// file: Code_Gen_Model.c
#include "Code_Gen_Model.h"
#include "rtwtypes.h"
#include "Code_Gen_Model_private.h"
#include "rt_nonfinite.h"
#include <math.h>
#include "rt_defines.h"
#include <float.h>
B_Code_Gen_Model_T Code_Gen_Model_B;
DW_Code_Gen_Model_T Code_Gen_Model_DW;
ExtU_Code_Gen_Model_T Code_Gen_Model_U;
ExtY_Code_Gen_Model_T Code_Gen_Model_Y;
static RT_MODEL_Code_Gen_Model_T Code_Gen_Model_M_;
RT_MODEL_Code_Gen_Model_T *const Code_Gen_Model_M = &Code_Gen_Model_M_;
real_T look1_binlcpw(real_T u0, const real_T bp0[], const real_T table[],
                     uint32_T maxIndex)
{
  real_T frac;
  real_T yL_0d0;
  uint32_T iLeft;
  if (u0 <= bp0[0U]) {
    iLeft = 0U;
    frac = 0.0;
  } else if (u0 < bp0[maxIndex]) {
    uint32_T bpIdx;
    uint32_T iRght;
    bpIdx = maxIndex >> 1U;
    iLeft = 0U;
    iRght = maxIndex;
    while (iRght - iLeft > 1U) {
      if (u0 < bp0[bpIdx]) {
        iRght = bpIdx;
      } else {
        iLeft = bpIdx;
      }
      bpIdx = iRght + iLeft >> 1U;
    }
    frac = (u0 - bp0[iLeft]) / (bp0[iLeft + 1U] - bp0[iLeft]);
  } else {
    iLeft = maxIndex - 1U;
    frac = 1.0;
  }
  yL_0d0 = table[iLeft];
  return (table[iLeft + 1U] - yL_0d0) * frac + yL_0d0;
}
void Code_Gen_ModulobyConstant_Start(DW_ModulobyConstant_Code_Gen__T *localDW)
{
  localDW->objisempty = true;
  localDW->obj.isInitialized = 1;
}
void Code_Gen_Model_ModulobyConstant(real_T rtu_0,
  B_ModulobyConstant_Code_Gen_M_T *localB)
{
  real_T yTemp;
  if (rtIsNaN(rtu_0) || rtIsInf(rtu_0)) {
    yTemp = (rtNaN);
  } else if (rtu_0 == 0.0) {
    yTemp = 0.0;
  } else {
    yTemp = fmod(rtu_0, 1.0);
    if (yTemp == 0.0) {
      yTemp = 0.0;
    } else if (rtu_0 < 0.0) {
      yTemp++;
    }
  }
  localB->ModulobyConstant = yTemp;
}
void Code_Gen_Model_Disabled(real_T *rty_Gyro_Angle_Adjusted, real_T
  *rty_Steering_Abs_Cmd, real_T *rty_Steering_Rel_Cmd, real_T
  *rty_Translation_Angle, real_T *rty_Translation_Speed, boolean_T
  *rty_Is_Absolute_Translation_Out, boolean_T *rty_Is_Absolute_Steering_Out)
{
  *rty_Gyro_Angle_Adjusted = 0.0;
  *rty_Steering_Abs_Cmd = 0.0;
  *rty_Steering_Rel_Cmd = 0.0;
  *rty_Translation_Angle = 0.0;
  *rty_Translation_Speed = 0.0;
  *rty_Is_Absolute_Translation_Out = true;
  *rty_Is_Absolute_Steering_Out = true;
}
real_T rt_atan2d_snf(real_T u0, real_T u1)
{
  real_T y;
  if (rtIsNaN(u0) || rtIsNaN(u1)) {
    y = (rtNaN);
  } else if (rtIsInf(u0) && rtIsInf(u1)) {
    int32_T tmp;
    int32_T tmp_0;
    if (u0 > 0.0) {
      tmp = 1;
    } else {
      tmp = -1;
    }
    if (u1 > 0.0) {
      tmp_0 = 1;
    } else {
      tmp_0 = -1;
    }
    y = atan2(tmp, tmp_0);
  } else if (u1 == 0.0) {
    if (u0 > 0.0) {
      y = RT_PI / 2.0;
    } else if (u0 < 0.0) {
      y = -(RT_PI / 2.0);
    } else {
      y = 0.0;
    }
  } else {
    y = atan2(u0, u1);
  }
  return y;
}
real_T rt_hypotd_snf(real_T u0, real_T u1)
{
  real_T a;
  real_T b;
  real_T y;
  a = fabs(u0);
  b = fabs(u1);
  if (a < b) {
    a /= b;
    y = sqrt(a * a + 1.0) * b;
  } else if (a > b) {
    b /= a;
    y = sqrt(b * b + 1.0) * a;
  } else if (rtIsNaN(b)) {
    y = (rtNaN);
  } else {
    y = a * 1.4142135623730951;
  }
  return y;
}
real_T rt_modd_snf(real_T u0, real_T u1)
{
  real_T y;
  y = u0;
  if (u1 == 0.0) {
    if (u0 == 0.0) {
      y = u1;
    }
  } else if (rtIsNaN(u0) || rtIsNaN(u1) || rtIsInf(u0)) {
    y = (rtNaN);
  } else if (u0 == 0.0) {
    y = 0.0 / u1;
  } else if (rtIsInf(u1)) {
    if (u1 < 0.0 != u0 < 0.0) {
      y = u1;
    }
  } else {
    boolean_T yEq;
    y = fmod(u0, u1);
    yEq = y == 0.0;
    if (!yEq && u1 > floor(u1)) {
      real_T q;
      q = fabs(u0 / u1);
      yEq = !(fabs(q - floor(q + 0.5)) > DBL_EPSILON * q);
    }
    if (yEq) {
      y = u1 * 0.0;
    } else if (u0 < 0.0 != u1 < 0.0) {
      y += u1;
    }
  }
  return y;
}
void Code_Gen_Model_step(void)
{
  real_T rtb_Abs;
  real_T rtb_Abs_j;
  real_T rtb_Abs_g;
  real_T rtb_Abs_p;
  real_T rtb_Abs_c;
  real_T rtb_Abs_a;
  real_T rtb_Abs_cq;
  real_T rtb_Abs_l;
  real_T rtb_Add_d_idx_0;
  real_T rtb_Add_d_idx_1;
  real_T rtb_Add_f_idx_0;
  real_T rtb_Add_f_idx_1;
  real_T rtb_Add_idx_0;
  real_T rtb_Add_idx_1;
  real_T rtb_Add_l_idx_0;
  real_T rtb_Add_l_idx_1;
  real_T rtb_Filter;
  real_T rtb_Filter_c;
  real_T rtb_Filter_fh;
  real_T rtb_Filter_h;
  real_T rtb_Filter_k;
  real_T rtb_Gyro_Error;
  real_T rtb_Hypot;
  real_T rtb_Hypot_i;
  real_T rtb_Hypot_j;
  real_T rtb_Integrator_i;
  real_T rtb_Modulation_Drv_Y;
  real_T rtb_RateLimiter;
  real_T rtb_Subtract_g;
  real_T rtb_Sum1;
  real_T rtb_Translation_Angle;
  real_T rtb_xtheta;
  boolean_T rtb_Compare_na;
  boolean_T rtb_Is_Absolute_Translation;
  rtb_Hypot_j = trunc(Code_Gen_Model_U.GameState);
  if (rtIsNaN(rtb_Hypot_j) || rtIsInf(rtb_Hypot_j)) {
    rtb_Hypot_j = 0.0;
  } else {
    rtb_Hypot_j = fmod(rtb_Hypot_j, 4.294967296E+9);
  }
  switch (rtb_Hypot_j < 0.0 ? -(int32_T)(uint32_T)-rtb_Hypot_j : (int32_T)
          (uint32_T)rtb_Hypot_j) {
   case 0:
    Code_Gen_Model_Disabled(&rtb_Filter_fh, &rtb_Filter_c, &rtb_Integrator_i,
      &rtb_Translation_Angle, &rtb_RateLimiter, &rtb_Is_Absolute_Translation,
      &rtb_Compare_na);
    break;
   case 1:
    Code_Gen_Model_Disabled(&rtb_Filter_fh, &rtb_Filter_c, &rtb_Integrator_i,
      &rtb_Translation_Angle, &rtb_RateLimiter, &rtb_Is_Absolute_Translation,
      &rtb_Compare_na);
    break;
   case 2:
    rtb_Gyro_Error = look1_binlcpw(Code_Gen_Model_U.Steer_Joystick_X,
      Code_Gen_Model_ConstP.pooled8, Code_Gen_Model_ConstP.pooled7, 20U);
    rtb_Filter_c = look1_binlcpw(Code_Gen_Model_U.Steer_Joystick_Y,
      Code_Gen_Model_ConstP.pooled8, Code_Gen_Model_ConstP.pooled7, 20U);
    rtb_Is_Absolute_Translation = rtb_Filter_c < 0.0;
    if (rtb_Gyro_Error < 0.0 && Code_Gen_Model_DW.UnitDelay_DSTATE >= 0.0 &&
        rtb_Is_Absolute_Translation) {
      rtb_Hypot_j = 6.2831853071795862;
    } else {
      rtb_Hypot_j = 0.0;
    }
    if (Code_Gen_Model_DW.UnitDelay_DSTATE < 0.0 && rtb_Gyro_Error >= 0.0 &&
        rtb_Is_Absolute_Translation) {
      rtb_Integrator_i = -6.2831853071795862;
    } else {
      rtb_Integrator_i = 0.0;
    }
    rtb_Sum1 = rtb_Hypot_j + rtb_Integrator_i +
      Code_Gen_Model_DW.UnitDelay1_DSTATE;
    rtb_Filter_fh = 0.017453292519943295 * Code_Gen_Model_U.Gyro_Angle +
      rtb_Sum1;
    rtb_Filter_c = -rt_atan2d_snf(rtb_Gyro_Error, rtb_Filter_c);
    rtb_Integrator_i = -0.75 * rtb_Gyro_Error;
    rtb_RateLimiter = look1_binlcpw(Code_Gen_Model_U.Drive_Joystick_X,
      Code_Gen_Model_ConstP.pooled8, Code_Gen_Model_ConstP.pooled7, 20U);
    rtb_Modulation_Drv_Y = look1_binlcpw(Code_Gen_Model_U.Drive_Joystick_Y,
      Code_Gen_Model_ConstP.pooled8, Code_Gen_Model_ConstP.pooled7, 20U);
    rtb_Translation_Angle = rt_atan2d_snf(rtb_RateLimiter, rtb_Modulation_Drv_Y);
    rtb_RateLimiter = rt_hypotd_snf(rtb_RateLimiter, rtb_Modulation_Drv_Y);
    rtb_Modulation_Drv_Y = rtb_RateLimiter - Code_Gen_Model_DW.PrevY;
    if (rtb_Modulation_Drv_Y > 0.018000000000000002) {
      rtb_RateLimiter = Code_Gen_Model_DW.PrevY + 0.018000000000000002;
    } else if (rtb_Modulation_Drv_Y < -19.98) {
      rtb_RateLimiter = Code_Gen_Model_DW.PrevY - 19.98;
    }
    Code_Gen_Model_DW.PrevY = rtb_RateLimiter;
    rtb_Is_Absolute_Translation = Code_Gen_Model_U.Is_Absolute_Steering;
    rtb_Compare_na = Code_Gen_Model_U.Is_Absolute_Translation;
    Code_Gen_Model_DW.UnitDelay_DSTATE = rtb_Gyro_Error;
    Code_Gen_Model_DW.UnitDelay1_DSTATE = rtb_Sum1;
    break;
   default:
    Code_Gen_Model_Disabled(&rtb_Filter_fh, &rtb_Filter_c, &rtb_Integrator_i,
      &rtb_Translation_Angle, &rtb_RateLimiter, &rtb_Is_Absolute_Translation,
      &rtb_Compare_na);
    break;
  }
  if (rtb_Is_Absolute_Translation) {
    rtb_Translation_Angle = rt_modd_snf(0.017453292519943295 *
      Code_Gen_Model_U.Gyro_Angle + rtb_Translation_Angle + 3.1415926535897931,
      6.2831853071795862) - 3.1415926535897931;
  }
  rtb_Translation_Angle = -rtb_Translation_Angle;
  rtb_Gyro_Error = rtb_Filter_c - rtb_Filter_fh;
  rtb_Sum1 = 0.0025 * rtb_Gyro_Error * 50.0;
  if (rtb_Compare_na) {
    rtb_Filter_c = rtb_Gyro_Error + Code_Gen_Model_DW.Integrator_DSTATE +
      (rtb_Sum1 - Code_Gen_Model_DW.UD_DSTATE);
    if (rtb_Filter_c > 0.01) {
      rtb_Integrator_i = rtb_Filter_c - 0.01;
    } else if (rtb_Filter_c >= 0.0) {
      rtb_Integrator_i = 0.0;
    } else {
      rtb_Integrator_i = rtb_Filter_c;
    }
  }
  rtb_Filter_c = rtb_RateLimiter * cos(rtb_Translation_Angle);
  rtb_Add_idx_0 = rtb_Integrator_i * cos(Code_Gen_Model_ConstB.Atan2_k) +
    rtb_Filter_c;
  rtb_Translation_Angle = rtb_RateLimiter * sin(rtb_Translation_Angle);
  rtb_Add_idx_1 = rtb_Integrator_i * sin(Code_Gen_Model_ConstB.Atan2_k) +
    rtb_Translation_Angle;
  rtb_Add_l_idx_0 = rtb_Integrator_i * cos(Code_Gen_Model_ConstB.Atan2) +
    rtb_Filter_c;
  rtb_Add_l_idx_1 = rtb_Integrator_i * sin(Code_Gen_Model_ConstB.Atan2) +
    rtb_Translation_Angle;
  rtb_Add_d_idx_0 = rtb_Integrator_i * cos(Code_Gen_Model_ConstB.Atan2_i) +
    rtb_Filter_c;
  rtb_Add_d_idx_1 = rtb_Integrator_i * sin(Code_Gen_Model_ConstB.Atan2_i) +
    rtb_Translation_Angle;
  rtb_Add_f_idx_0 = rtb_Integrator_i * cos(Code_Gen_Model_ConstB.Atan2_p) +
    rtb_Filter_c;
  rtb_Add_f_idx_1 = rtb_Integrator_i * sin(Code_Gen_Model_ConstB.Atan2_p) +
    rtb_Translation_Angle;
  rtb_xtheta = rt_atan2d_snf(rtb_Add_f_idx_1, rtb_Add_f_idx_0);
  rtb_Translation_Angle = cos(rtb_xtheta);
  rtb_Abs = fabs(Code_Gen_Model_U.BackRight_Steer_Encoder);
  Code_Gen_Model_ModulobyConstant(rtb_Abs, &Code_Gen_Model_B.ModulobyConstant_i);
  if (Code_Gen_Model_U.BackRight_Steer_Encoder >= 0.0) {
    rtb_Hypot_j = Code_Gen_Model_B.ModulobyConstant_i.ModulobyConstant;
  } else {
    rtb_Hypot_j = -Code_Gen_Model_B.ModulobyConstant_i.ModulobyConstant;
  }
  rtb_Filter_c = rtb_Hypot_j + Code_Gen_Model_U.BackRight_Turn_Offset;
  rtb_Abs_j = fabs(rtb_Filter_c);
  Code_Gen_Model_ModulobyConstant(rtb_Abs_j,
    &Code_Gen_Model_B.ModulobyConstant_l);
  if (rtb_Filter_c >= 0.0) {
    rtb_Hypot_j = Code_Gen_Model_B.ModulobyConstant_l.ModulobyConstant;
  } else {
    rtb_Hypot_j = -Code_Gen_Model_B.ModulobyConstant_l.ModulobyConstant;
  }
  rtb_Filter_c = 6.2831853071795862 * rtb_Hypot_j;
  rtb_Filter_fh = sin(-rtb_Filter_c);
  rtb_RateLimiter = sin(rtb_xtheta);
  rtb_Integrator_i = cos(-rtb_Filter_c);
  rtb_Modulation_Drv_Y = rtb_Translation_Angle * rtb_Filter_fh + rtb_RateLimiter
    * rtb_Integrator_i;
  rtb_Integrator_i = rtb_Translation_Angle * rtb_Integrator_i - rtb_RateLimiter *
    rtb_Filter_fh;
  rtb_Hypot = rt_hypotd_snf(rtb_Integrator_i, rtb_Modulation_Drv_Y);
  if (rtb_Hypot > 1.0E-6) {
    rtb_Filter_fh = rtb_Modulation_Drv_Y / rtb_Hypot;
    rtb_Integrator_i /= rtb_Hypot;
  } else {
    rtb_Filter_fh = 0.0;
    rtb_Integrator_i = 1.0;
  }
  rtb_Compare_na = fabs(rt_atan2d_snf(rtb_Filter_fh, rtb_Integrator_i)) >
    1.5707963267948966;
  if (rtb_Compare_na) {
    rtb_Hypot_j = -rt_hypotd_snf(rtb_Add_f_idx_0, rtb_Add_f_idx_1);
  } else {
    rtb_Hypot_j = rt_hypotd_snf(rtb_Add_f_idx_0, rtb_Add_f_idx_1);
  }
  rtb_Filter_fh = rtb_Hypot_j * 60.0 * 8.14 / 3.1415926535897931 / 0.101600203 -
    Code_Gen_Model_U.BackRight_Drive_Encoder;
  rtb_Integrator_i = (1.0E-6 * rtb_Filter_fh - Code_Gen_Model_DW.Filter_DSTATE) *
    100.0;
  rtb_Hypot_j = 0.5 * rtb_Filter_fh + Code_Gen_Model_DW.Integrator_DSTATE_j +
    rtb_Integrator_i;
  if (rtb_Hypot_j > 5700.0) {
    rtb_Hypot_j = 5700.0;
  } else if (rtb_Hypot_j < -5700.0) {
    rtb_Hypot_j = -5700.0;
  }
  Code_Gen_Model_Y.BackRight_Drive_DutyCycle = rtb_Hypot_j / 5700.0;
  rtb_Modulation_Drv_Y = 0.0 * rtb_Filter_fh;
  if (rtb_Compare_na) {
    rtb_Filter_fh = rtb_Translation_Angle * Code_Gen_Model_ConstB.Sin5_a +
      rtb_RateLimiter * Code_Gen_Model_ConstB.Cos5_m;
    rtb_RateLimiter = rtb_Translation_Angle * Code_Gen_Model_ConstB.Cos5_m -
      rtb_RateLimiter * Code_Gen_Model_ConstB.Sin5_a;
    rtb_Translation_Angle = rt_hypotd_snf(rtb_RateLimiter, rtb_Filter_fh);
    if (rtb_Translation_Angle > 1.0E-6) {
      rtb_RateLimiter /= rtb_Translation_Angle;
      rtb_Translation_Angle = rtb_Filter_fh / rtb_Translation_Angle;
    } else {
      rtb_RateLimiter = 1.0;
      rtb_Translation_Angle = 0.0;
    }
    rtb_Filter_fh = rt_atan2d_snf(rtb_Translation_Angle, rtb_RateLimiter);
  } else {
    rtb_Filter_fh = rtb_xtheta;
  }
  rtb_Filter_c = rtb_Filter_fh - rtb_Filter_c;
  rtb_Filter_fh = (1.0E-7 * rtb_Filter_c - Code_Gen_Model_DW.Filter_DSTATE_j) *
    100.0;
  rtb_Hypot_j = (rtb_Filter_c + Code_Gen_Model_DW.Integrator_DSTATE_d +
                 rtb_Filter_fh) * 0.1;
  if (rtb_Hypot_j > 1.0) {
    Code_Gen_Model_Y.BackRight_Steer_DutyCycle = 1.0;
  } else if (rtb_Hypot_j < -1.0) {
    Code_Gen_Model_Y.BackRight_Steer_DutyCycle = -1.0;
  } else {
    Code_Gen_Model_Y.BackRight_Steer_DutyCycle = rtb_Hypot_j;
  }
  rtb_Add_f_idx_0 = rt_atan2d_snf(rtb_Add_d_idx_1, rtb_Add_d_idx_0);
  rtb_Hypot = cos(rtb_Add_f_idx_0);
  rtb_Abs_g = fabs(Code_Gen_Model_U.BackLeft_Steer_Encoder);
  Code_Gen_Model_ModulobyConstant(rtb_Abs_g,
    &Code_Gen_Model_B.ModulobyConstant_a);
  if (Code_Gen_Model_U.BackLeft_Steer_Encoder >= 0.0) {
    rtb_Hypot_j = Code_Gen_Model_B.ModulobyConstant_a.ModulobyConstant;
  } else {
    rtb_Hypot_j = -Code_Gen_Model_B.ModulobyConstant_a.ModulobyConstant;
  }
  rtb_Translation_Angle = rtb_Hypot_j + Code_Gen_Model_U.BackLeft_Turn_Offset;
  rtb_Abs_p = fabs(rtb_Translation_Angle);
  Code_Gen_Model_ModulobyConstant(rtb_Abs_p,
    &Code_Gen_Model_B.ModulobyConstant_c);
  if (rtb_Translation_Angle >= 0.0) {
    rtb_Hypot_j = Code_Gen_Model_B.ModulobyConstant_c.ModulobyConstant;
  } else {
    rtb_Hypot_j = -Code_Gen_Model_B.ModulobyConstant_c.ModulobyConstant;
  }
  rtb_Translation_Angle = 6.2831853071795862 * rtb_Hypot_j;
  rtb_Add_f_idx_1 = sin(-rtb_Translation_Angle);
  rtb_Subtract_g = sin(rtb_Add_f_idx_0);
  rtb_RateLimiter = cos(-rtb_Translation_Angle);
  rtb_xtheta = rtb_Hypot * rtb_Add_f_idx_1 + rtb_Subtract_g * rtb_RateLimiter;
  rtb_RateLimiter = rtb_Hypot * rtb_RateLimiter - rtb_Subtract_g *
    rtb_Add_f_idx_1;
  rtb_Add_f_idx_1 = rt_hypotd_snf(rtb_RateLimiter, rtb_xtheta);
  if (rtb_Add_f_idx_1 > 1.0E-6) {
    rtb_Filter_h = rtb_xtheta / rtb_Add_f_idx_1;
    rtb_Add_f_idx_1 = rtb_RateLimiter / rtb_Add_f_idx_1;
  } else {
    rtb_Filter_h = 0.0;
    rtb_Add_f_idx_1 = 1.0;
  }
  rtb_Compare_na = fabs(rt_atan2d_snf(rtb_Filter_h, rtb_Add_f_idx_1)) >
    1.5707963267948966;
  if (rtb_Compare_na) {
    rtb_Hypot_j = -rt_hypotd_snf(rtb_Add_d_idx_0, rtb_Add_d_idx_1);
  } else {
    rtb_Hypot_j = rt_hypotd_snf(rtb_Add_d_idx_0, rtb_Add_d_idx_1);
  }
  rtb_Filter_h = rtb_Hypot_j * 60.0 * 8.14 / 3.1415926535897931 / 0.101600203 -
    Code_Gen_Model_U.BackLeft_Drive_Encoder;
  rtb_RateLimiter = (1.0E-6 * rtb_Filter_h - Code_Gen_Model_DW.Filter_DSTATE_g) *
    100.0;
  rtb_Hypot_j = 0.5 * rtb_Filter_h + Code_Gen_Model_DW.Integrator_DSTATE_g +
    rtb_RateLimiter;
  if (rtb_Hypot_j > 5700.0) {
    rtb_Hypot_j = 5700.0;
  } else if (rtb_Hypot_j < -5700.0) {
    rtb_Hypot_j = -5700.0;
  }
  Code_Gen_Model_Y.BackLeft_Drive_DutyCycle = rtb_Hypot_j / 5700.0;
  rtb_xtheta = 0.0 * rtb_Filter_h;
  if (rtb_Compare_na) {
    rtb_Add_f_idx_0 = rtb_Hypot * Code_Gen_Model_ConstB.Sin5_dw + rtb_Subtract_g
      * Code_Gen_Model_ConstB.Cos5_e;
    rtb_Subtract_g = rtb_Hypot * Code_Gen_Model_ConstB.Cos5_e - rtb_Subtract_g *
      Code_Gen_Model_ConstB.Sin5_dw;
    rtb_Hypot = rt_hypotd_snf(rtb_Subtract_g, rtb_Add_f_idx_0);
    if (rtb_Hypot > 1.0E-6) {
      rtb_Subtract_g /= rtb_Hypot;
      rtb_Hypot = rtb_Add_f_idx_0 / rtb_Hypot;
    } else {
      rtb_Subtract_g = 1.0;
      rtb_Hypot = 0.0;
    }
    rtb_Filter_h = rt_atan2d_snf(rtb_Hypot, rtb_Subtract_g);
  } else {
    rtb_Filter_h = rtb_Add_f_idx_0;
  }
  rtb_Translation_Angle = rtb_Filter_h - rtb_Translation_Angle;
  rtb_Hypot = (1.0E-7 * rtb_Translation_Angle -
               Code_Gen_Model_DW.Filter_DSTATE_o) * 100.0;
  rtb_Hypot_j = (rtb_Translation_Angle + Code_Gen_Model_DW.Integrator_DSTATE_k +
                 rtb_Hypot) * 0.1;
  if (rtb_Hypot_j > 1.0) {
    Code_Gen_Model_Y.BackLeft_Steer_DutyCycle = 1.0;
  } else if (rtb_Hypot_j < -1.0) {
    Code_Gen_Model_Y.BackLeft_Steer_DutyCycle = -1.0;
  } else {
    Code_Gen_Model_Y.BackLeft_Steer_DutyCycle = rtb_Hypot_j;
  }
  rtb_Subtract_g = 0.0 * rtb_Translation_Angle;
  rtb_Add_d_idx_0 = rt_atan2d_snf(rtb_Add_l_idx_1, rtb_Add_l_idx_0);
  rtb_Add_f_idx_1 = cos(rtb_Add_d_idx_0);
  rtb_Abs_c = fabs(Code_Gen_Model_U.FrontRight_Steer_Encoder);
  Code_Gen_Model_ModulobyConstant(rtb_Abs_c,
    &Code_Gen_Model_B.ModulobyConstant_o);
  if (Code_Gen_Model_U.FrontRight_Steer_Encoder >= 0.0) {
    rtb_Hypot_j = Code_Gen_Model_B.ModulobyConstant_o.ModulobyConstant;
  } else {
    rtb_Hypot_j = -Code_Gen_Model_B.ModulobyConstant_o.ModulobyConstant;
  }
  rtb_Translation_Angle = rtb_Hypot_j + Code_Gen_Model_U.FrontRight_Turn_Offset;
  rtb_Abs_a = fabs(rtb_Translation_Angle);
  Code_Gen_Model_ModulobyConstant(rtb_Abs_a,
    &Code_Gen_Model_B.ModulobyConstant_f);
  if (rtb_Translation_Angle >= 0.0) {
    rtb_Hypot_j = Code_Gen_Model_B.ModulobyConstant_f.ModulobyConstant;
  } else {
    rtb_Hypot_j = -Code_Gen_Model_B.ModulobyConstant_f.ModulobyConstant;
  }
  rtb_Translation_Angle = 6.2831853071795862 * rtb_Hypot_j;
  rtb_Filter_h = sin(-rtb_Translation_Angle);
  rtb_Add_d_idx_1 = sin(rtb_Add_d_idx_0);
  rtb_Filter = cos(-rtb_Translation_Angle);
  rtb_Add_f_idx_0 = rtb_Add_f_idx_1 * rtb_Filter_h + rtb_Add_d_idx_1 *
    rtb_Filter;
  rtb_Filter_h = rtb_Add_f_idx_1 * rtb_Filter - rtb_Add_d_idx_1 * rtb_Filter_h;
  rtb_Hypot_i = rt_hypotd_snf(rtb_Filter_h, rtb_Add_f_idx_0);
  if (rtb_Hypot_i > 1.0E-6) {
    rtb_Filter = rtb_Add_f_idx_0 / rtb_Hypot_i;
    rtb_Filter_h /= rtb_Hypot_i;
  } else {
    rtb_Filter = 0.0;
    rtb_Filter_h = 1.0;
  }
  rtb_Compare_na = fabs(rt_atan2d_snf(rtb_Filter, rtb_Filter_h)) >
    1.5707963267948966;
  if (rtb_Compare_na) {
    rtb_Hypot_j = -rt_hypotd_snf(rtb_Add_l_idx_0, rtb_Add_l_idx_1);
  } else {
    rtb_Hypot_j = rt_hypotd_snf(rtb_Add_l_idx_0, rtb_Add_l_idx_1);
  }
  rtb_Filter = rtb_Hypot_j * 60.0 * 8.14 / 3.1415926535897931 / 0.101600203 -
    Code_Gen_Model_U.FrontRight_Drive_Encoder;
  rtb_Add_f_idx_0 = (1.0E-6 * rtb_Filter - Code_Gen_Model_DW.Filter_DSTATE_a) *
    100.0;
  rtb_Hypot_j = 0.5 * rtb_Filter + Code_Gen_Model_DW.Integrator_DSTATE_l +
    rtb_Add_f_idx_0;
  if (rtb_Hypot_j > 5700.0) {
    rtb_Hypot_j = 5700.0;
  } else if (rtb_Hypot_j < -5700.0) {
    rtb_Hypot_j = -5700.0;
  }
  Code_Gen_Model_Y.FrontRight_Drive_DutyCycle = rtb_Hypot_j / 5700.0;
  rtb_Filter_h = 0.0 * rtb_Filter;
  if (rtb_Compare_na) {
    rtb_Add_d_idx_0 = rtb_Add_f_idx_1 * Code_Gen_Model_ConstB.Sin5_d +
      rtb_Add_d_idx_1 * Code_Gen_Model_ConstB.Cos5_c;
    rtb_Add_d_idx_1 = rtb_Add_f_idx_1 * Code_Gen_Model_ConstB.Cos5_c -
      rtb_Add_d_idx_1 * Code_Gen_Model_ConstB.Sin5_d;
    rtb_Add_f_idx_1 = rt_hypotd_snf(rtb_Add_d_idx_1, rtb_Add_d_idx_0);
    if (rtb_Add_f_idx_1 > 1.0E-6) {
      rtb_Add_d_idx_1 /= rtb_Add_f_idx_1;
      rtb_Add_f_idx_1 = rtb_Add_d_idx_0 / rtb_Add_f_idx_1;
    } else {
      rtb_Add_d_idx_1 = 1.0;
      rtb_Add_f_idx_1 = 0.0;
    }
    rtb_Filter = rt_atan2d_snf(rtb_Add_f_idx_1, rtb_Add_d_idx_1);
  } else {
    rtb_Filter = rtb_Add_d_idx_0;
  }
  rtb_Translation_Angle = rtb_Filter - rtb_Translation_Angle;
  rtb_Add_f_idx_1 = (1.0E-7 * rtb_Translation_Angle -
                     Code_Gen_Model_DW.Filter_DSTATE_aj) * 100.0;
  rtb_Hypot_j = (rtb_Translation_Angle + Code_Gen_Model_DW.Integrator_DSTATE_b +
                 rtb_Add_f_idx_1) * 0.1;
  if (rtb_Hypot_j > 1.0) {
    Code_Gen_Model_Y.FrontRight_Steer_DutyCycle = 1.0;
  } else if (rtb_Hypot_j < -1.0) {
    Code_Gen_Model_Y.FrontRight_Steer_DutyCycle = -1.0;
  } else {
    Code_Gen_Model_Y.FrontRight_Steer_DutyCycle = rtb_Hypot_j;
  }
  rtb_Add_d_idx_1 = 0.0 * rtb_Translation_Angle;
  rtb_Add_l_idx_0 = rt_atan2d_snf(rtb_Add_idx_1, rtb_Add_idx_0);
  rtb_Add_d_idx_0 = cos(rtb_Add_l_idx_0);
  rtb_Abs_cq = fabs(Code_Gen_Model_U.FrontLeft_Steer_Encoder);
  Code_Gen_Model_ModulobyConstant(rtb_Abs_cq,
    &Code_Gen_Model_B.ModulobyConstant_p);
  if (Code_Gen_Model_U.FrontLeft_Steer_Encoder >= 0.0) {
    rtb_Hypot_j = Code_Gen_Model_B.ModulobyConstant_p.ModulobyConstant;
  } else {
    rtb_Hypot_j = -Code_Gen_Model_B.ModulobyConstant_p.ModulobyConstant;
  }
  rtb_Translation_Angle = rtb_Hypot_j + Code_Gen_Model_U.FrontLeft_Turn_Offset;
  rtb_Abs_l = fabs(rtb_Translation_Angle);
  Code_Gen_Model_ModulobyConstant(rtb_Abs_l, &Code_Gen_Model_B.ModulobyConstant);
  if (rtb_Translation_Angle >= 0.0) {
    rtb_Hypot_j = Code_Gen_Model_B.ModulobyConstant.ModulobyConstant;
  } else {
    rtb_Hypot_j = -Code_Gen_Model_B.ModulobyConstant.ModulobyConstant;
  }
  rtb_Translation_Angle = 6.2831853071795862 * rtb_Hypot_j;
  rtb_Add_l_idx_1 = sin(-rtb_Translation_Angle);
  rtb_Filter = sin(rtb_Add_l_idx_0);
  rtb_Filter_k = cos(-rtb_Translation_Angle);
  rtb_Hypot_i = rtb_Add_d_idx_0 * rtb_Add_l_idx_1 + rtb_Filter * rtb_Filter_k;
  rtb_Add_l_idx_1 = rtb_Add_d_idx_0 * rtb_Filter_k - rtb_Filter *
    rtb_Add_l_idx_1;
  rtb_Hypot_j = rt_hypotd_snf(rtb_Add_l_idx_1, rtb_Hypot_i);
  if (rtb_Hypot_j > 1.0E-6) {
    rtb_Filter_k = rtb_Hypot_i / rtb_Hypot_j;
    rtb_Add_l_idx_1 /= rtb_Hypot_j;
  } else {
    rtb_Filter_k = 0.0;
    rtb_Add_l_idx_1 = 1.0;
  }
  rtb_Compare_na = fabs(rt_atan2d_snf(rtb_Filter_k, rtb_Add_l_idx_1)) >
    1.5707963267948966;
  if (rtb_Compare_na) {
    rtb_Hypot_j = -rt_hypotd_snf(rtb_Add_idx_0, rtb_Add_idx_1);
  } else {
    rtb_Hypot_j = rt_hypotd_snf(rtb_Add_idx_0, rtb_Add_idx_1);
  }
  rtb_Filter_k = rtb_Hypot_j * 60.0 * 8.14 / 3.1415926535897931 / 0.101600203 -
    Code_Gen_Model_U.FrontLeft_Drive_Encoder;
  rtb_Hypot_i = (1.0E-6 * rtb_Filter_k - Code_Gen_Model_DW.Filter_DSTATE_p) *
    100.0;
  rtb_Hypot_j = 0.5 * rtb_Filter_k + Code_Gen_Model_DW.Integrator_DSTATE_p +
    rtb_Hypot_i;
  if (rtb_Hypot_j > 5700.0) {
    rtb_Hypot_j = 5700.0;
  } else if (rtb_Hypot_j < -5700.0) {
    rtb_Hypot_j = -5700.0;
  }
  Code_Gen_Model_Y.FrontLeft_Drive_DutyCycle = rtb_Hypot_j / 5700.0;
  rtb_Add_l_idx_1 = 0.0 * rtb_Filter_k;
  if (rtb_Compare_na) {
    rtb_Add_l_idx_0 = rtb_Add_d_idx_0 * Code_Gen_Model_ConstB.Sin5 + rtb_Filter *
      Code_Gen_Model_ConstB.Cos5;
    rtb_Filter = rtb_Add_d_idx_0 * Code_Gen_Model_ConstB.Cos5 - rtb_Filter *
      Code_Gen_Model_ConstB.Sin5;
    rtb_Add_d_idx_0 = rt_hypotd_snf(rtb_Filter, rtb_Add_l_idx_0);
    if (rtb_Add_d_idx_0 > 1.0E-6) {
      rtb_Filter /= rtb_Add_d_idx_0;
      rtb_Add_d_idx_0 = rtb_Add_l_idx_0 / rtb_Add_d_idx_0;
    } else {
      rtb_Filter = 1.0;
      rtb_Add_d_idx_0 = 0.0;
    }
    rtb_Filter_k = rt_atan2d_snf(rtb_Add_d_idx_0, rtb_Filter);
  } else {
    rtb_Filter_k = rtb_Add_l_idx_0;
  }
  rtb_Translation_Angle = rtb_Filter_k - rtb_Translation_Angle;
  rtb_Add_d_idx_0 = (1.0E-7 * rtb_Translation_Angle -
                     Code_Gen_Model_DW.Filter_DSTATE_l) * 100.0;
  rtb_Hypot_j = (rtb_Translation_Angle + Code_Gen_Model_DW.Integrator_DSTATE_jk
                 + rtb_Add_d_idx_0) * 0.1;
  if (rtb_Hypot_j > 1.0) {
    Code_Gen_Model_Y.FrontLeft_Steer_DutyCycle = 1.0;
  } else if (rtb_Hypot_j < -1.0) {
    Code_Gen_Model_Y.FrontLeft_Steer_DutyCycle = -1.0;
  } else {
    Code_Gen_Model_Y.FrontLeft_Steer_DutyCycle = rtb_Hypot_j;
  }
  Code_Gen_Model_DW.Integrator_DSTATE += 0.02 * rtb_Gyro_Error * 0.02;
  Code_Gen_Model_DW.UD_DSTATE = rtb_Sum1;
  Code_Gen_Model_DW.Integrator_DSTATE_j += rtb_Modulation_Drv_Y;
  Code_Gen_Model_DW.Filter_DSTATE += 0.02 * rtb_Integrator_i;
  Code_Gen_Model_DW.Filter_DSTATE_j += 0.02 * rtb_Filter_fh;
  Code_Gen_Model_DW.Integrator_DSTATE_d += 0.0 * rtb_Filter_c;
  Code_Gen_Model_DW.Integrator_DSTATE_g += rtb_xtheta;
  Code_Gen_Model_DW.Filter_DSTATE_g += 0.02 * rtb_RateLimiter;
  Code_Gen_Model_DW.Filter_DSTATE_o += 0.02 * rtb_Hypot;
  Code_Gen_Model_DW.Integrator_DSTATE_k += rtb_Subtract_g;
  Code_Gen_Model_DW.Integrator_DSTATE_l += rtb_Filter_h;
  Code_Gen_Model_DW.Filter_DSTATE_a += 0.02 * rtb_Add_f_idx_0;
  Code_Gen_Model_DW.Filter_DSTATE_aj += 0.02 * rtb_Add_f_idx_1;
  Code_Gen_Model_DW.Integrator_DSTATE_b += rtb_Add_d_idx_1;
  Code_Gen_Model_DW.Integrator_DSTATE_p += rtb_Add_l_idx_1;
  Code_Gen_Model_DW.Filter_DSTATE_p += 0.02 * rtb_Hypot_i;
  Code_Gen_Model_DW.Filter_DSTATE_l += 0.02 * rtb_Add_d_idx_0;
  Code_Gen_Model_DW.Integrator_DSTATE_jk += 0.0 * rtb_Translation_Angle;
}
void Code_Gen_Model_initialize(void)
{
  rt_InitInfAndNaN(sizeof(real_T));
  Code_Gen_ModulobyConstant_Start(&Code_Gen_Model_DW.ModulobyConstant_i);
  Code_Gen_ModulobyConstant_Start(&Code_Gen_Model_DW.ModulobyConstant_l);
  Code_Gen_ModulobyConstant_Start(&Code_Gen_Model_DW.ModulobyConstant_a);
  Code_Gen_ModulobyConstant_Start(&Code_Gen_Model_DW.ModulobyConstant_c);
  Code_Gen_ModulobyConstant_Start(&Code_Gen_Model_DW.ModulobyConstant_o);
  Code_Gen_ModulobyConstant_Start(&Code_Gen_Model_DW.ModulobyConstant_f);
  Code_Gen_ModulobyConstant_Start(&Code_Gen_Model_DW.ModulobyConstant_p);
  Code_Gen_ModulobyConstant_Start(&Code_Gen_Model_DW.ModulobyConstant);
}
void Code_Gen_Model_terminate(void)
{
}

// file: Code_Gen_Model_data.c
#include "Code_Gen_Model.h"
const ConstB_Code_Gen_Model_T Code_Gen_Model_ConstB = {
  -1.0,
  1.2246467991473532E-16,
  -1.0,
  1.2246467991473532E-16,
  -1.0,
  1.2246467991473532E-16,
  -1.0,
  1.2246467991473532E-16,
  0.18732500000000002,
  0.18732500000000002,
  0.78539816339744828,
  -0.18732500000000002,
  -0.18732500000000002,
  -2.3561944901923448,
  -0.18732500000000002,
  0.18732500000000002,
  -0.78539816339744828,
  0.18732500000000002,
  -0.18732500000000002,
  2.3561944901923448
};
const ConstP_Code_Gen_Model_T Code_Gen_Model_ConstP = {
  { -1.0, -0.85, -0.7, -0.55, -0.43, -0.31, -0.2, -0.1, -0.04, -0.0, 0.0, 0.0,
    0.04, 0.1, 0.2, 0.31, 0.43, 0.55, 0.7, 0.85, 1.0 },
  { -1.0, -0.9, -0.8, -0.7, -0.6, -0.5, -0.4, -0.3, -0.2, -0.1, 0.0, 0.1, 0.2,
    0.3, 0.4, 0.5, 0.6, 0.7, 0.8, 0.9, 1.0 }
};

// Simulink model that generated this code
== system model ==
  GameState : Inport
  Steer_Joystick_X : Inport
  Steer_Joystick_Y : Inport
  Drive_Joystick_X : Inport
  Drive_Joystick_Y : Inport
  Gyro_Angle : Inport
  FrontLeft_Drive_Encoder : Inport
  FrontRight_Drive_Encoder : Inport
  BackLeft_Drive_Encoder : Inport
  BackRight_Drive_Encoder : Inport
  FrontLeft_Steer_Encoder : Inport
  FrontRight_Steer_Encoder : Inport
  BackLeft_Steer_Encoder : Inport
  BackRight_Steer_Encoder : Inport
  FrontLeft_Turn_Offset : Inport
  FrontRight_Turn_Offset : Inport
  BackLeft_Turn_Offset : Inport
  BackRight_Turn_Offset : Inport
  Is_Absolute_Steering : Inport
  Is_Absolute_Translation : Inport
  FrontLeft_Drive_DutyCycle : Outport  <- 1: Control#1
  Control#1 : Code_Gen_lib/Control  <- 1: GameState, 2: Steer_Joystick_X, 3: Steer_Joystick_Y, 4: Drive_Joystick_X, 5: Drive_Joystick_Y, 6: Gyro_Angle, 7: FrontLeft_Drive_Encoder, 8: FrontRight_Drive_Encoder, 9: BackLeft_Drive_Encoder, 10: BackRight_Drive_Encoder, 11: FrontLeft_Steer_Encoder, 12: FrontRight_Steer_Encoder, 13: BackLeft_Steer_Encoder, 14: BackRight_Steer_Encoder, 15: FrontLeft_Turn_Offset, 16: FrontRight_Turn_Offset, 17: BackLeft_Turn_Offset, 18: BackRight_Turn_Offset, 19: Is_Absolute_Steering, 20: Is_Absolute_Translation
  FrontLeft_Steer_DutyCycle : Outport  <- 1: Control#1/2
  FrontRight_Drive_DutyCycle : Outport  <- 1: Control#1/3
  FrontRight_Steer_DutyCycle : Outport  <- 1: Control#1/4
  BackLeft_Drive_DutyCycle : Outport  <- 1: Control#1/5
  BackLeft_Steer_DutyCycle : Outport  <- 1: Control#1/6
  BackRight_Drive_DutyCycle : Outport  <- 1: Control#1/7
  BackRight_Steer_DutyCycle : Outport  <- 1: Control#1/8
